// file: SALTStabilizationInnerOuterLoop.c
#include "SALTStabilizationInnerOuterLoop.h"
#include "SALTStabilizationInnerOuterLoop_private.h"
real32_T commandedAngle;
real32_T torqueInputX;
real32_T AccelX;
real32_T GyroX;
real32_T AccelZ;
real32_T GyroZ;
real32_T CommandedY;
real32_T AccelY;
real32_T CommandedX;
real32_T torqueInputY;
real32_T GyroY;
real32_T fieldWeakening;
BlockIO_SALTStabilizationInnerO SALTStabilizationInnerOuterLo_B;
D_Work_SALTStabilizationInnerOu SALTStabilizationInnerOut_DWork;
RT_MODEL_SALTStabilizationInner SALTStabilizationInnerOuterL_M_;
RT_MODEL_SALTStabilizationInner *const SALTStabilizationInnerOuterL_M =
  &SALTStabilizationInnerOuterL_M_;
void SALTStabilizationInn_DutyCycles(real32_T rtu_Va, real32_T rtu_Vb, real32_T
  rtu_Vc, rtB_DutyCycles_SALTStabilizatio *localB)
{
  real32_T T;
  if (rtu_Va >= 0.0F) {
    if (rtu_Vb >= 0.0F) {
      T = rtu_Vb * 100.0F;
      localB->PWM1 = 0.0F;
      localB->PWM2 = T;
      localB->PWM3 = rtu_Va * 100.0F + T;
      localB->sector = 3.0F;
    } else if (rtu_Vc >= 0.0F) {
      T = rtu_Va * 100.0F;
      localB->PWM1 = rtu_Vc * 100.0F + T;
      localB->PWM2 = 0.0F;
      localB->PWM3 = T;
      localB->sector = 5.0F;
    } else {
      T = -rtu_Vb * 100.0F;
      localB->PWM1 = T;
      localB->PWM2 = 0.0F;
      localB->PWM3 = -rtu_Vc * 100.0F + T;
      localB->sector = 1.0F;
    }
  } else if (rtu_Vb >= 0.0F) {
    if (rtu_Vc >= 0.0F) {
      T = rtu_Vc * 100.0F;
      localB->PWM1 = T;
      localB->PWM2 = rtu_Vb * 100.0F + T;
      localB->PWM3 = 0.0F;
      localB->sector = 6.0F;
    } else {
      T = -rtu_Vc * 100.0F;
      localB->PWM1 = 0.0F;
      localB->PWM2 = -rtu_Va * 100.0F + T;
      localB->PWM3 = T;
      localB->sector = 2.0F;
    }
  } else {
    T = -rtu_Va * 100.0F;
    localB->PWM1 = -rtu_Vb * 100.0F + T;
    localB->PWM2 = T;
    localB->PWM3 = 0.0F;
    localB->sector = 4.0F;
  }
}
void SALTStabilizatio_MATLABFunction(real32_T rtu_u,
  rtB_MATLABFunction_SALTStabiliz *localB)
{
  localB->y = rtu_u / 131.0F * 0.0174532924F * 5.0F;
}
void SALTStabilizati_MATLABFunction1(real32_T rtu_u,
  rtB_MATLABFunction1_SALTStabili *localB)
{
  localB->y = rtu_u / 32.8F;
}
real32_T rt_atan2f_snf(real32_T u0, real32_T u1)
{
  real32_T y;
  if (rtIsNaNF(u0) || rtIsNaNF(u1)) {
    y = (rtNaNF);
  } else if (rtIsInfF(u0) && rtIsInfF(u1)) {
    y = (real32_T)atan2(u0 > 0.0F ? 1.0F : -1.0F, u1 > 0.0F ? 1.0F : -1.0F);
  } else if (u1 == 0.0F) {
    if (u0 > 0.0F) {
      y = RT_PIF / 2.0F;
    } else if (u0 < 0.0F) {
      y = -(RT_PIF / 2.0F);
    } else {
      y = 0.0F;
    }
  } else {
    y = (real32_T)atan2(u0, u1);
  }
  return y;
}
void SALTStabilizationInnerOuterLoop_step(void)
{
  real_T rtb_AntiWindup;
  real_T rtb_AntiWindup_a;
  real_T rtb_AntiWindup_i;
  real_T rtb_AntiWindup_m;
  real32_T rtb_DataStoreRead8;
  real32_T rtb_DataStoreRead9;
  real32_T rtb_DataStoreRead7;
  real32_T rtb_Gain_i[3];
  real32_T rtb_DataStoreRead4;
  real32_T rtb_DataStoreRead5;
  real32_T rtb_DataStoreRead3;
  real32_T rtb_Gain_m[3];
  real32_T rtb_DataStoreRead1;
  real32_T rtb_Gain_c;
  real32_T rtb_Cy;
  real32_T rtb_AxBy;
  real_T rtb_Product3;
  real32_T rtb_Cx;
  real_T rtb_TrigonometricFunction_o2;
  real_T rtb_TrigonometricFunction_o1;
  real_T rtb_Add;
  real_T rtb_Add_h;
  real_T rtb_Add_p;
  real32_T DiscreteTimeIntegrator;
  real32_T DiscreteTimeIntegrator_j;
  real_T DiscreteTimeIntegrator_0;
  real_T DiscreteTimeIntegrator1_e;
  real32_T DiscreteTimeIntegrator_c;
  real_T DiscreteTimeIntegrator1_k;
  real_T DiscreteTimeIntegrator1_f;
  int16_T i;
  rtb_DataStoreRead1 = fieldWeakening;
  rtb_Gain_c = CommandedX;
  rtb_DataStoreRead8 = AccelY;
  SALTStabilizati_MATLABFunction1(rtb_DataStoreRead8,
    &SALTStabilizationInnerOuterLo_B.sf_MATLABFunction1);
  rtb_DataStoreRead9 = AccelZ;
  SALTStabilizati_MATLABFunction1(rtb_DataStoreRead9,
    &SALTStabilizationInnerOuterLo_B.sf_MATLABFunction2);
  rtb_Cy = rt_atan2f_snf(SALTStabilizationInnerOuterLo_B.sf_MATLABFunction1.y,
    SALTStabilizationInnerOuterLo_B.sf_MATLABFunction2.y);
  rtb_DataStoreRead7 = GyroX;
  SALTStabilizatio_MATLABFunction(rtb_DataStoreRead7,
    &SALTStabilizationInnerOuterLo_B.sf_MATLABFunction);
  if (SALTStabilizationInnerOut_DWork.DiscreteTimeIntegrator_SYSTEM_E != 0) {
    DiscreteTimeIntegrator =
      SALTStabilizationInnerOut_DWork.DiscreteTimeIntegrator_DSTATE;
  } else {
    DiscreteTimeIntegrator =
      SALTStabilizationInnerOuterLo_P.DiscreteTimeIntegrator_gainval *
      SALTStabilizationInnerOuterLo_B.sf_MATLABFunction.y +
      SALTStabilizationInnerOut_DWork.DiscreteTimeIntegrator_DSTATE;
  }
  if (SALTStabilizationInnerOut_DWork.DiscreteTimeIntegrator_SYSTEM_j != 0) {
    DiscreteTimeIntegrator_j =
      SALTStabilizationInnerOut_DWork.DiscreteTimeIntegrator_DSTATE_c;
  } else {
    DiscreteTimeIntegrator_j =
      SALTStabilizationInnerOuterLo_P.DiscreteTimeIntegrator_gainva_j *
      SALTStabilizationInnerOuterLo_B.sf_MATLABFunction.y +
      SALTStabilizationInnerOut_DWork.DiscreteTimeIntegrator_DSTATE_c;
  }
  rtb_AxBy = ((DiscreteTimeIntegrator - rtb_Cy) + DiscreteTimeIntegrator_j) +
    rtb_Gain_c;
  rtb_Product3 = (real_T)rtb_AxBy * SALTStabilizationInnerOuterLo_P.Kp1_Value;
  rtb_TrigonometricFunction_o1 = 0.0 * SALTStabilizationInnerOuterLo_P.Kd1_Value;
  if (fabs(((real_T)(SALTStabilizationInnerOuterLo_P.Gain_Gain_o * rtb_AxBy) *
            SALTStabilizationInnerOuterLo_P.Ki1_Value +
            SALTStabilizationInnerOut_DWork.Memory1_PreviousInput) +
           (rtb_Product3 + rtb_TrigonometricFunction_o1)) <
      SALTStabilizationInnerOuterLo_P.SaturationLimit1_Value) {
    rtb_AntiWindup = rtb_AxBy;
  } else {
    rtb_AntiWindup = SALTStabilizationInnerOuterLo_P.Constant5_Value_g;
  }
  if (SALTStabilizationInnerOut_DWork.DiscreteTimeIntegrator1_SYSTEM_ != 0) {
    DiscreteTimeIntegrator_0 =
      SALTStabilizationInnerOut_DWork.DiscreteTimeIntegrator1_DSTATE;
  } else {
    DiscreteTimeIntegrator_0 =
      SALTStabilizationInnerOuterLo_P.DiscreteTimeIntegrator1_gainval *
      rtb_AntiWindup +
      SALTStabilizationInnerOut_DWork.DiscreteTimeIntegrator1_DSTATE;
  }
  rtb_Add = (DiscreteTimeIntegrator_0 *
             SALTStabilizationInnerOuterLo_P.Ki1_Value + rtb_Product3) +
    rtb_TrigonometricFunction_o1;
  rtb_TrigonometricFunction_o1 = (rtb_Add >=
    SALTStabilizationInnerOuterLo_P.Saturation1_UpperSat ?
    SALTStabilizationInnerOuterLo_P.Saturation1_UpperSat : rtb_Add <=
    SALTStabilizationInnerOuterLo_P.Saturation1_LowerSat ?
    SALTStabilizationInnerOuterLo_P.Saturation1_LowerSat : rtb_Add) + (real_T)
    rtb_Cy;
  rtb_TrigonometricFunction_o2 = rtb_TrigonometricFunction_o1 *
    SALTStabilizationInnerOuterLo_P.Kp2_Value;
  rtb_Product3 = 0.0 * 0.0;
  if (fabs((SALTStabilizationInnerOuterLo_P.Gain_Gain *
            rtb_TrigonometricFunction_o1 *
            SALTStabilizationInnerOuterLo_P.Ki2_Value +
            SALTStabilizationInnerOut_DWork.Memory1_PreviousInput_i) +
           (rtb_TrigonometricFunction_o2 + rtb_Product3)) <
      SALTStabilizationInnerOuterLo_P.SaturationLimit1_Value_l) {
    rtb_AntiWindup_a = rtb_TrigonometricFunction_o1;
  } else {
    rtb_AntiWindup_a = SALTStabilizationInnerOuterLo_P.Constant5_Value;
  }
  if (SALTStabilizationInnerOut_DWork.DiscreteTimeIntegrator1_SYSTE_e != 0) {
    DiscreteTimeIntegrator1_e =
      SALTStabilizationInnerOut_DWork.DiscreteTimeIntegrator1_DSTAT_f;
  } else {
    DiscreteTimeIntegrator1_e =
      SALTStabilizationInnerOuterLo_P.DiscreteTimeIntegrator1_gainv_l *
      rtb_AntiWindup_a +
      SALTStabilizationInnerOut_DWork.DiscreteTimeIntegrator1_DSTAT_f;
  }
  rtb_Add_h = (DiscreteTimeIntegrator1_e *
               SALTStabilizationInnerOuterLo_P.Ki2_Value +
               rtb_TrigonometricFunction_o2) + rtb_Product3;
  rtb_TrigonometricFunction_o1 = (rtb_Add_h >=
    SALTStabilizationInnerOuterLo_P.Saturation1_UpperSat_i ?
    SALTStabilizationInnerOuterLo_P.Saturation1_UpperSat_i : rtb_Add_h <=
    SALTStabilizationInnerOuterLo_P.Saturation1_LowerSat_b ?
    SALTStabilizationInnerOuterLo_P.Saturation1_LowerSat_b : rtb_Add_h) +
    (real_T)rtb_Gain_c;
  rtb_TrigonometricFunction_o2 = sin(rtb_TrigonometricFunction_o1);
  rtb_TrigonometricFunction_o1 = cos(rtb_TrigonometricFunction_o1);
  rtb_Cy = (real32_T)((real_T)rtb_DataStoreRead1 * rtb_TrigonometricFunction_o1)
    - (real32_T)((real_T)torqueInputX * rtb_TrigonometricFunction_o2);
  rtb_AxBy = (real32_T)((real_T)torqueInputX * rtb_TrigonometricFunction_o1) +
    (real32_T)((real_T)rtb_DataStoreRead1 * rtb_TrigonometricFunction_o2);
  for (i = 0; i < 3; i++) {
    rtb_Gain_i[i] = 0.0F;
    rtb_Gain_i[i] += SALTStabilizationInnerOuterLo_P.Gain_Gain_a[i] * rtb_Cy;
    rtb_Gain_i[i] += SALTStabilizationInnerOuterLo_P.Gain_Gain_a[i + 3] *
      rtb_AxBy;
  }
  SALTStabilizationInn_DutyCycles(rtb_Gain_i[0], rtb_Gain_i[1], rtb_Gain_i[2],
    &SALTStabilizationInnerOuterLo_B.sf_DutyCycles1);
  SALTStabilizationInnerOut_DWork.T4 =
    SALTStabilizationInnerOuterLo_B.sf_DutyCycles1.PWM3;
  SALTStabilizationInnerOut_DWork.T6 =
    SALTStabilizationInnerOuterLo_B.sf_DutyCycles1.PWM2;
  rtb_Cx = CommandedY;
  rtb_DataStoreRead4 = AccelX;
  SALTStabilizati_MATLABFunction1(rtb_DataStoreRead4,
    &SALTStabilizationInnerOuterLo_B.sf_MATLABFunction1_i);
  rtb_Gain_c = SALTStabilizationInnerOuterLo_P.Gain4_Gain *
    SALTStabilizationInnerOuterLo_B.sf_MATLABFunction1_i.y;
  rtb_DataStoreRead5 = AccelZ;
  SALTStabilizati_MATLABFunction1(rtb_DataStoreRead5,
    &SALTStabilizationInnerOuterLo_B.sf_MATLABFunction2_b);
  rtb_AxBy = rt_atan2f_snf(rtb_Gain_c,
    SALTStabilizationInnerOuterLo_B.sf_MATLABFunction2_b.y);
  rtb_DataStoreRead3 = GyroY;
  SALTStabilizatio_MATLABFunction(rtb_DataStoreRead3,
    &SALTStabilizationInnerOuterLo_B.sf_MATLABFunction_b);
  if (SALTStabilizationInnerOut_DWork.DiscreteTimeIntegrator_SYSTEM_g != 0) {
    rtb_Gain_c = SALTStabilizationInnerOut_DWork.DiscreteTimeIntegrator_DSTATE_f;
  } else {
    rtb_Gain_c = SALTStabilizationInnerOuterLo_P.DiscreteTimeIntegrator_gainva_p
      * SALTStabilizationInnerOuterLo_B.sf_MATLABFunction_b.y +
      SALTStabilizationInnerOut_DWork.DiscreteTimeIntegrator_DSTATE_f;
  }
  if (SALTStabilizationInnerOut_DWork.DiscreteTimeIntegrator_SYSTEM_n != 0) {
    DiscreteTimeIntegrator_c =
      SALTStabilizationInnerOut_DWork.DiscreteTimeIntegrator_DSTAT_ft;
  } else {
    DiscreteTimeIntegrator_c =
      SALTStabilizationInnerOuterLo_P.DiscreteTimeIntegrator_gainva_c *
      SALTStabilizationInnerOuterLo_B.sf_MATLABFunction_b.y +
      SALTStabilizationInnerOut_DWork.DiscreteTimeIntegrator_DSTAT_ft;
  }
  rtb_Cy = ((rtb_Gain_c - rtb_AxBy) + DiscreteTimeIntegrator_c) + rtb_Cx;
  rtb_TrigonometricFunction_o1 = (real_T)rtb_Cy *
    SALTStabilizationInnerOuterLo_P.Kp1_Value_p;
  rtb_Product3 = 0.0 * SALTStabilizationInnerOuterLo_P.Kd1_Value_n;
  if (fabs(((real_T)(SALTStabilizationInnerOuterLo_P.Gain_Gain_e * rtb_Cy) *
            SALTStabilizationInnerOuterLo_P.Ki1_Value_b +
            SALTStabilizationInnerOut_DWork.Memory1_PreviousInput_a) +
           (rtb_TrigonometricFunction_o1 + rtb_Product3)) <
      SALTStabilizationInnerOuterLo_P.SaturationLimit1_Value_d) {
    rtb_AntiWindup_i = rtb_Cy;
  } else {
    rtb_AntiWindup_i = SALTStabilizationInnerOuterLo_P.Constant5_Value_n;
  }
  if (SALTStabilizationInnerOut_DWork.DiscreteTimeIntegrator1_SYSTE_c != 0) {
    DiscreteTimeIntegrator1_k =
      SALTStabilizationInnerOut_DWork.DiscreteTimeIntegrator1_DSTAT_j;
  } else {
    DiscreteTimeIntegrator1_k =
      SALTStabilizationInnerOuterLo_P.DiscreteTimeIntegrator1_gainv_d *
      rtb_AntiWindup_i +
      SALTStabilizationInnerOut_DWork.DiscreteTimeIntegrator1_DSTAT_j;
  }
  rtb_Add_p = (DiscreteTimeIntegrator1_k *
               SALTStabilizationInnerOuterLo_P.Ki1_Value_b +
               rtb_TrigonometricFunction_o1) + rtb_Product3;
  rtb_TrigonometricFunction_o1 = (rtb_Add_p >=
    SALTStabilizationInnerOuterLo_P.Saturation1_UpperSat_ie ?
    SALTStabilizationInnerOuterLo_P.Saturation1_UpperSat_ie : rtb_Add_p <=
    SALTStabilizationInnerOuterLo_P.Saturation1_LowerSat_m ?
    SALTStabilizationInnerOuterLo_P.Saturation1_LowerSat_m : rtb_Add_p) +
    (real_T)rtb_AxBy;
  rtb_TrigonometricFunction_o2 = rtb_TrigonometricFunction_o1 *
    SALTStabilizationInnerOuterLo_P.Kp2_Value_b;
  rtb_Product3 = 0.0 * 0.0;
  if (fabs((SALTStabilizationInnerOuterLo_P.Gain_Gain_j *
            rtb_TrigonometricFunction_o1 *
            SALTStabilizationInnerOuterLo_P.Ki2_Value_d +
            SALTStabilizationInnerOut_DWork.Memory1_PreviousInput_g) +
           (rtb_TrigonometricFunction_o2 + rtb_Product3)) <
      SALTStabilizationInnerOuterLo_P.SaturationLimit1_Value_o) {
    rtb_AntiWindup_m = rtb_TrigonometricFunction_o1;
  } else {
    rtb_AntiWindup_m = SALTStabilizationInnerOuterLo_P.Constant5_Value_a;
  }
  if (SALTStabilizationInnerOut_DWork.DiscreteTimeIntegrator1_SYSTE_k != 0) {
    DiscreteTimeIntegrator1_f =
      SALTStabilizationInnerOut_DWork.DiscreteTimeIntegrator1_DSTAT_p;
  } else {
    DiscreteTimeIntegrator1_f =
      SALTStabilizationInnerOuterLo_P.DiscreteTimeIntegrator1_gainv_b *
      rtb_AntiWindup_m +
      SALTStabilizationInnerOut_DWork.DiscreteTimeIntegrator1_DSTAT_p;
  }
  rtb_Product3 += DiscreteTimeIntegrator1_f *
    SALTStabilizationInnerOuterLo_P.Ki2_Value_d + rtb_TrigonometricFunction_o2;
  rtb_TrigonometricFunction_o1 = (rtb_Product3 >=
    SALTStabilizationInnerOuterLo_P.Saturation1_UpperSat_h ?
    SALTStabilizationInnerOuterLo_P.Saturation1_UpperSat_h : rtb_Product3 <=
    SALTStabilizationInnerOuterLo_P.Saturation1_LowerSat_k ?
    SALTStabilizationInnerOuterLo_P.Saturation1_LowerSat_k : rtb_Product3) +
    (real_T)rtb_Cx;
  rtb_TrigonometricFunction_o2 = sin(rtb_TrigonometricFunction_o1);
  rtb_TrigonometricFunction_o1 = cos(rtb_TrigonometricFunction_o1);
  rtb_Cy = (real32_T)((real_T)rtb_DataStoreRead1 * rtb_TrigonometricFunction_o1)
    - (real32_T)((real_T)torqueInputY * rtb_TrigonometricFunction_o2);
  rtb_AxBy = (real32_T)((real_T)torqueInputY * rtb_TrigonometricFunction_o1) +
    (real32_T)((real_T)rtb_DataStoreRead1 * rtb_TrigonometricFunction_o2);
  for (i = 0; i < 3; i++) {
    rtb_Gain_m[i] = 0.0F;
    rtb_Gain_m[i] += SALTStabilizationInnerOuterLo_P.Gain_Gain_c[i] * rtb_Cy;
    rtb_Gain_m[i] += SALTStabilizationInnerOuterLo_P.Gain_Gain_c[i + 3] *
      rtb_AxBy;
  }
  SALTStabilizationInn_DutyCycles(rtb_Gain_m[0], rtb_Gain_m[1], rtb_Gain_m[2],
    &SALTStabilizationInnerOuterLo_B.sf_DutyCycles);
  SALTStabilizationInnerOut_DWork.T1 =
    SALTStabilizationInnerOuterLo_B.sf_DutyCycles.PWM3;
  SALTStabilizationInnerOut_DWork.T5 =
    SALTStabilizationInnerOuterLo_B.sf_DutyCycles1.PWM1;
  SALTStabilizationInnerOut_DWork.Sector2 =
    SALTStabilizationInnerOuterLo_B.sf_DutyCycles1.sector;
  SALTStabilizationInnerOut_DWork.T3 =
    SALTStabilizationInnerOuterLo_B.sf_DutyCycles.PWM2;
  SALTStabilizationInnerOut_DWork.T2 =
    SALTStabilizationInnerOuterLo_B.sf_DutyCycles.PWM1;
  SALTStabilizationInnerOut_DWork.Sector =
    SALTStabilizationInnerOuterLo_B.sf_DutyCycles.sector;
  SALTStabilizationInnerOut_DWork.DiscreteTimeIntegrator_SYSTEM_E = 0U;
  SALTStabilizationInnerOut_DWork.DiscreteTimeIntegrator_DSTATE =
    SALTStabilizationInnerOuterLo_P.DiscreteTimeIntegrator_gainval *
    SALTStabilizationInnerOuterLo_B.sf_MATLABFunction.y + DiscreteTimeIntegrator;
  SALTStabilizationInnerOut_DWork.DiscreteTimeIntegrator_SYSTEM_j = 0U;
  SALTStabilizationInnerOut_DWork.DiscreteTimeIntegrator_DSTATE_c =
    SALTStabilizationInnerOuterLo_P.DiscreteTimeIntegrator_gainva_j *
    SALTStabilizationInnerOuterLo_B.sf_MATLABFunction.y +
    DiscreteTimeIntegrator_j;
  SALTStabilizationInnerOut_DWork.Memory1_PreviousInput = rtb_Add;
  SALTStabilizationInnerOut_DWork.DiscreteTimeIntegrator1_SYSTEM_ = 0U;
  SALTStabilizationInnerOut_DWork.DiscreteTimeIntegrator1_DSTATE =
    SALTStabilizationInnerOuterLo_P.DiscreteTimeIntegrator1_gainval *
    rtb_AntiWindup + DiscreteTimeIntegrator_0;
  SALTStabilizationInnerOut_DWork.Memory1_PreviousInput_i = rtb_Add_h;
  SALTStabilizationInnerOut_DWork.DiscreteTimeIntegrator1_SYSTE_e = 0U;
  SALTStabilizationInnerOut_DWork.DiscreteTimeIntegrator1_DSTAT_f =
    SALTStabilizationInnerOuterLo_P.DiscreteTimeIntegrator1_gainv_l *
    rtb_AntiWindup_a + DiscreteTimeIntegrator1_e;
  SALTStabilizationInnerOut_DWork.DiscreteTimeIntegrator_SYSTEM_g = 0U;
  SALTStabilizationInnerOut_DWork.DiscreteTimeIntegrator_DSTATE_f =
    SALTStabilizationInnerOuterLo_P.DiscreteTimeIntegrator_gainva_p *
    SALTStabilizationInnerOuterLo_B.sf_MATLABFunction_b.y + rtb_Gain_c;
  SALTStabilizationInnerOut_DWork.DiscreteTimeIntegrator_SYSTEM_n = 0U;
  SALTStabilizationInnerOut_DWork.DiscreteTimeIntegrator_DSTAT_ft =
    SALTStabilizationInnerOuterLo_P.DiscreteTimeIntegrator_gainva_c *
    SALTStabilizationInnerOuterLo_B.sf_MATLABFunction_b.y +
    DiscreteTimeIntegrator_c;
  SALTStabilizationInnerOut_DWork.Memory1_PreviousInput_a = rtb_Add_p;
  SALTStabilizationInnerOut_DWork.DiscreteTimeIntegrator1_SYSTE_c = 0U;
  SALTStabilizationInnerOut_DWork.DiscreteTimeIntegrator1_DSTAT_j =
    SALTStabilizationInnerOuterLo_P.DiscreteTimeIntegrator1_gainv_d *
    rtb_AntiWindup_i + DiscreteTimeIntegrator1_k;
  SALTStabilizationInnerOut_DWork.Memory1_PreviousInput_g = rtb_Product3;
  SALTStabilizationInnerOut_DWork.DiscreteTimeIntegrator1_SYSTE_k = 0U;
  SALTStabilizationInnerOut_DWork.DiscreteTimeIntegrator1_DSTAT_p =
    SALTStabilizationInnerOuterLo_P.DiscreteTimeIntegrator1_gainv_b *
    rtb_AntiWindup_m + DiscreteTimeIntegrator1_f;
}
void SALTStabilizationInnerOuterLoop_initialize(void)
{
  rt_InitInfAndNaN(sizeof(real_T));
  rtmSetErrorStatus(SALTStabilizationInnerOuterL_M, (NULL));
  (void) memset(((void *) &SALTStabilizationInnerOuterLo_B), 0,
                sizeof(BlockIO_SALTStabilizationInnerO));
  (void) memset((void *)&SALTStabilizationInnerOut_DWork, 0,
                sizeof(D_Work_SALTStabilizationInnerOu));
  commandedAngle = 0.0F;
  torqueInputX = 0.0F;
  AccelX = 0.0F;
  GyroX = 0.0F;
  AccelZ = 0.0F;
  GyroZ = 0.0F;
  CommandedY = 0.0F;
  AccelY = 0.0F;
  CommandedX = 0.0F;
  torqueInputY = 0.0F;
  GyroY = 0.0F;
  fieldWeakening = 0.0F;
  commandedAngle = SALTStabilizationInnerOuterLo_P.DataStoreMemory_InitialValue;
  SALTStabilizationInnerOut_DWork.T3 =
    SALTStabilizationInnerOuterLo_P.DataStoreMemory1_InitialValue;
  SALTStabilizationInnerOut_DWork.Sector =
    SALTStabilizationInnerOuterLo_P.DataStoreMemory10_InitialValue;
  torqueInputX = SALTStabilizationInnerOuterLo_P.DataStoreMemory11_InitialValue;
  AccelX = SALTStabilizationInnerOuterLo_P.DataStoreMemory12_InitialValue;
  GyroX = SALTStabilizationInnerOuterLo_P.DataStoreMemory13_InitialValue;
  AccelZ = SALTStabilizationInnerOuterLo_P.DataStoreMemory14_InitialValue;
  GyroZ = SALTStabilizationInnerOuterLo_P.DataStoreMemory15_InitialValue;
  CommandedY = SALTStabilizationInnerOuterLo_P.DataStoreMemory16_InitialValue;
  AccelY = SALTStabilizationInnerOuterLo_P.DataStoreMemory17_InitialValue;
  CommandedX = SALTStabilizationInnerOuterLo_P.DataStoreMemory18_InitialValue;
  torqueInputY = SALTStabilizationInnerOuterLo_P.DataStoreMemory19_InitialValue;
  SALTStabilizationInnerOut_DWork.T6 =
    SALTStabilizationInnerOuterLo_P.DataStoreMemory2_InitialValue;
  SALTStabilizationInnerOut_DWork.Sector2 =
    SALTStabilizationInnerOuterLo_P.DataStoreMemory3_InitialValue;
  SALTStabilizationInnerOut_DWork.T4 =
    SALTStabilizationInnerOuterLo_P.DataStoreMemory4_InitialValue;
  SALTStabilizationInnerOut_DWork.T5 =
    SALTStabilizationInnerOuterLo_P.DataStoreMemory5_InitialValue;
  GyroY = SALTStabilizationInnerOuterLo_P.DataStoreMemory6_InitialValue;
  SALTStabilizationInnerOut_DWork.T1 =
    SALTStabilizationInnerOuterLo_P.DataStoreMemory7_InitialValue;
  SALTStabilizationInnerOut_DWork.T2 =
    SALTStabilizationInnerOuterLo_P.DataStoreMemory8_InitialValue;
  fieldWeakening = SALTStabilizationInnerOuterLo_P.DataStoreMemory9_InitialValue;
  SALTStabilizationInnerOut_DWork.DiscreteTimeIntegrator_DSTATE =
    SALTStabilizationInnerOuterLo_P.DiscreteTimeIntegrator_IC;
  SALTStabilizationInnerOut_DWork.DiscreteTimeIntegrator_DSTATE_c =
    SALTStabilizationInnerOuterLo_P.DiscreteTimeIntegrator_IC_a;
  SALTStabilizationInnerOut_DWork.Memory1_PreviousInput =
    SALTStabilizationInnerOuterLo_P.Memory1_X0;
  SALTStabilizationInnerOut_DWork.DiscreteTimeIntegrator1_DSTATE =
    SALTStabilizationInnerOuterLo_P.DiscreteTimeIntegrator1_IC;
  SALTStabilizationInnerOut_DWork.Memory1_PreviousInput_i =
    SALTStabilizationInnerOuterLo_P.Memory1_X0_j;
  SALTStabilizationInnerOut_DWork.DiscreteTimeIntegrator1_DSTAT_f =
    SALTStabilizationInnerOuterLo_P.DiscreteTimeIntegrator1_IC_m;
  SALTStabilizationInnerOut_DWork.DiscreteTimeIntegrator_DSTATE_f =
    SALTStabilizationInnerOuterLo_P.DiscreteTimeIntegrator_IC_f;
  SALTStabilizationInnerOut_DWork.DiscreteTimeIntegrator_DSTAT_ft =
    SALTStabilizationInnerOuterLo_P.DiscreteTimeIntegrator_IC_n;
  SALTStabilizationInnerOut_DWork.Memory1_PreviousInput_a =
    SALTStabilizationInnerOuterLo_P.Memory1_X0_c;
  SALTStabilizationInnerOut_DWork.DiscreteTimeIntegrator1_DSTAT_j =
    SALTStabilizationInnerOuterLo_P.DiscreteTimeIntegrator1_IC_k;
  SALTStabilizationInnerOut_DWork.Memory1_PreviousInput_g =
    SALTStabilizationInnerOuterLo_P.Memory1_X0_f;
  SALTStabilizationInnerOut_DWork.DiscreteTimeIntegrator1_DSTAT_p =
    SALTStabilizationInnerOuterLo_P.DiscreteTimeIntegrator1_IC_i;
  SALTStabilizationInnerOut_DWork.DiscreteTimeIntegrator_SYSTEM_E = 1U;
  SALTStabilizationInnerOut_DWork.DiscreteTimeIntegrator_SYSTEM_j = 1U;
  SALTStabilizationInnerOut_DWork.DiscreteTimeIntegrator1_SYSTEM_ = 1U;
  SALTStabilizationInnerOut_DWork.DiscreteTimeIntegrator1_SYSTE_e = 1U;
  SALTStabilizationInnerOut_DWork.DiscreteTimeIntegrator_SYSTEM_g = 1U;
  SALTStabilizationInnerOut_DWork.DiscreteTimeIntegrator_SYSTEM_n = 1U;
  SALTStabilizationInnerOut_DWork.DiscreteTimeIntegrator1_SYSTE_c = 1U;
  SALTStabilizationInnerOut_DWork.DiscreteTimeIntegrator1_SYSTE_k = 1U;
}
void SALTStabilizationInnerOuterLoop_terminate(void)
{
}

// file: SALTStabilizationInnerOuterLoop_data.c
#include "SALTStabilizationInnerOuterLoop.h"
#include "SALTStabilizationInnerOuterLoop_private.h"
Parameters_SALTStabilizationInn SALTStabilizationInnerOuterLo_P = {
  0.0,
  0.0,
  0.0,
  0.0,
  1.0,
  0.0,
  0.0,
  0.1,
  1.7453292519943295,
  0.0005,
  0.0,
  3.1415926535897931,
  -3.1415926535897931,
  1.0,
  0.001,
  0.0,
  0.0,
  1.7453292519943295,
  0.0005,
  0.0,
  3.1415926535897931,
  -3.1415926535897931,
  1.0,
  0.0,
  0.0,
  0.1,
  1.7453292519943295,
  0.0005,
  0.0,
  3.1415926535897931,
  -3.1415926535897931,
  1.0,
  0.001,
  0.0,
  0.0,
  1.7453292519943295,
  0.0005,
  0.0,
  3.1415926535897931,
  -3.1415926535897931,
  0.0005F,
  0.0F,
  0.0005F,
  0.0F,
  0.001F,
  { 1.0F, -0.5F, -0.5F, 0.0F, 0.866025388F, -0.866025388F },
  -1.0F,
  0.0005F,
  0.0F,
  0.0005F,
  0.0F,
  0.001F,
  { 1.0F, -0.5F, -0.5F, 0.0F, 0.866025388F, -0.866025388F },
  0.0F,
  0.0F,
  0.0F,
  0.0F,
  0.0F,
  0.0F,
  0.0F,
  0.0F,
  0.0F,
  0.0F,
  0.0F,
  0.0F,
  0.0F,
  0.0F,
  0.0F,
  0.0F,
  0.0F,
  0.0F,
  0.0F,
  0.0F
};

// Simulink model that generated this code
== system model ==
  DataStoreMemory : DataStoreMemory  DataStoreName=commandedAngle
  DataStoreMemory11 : DataStoreMemory  DataStoreName=torqueInputX
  DataStoreMemory12 : DataStoreMemory  DataStoreName=AccelX
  DataStoreMemory13 : DataStoreMemory  DataStoreName=GyroX
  DataStoreMemory14 : DataStoreMemory  DataStoreName=AccelZ
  DataStoreMemory15 : DataStoreMemory  DataStoreName=GyroZ
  DataStoreMemory16 : DataStoreMemory  DataStoreName=CommandedY
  DataStoreMemory17 : DataStoreMemory  DataStoreName=AccelY
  DataStoreMemory18 : DataStoreMemory  DataStoreName=CommandedX
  DataStoreMemory19 : DataStoreMemory  DataStoreName=torqueInputY
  DataStoreMemory6 : DataStoreMemory  DataStoreName=GyroY
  DataStoreMemory9 : DataStoreMemory  DataStoreName=fieldWeakening
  DataStoreWrite#1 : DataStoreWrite  DataStoreName=T4  <- 1: DutyCycles1/3
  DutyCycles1 : MATLAB Function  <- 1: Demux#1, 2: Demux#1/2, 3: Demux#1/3
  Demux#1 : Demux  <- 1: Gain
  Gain : Gain  Gain=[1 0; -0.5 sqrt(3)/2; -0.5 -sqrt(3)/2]  Multiplication=Matrix(K*u)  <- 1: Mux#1
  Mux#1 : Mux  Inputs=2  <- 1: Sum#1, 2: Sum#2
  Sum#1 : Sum  Inputs=+-  <- 1: Product#1, 2: Product#2
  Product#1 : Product  <- 1: DataStoreRead1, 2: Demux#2
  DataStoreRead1 : DataStoreRead  DataStoreName=fieldWeakening
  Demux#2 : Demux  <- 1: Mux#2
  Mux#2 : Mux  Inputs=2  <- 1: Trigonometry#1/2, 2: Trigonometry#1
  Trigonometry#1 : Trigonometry  Operator=sincos  <- 1: Sum#3
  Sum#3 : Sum  <- 1: DataStoreRead#1, 2: Saturation1
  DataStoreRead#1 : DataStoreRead  DataStoreName=CommandedX
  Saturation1 : Saturate  UpperLimit=pi  LowerLimit=-pi  <- 1: Add
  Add : Sum  Inputs=+++  <- 1: Product#3, 2: Product#4, 3: Product3
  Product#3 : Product  <- 1: Sum#4, 2: Kp2
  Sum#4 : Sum  <- 1: TrigonometricFunction, 2: Saturate#1
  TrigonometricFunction : Trigonometry  Operator=atan2  <- 1: MATLABFunction1, 2: MATLABFunction2
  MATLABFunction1 : MATLAB Function  <- 1: DataTypeConversion#1
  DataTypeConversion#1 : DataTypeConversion  <- 1: DataStoreRead8
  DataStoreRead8 : DataStoreRead  DataStoreName=AccelY
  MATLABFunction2 : MATLAB Function  <- 1: DataTypeConversion#2
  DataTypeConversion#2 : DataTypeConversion  <- 1: DataStoreRead9
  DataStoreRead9 : DataStoreRead  DataStoreName=AccelZ
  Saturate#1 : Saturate  UpperLimit=pi  LowerLimit=-pi  <- 1: Sum#5
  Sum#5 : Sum  Inputs=+++  <- 1: Product#5, 2: Product#6, 3: Product#7
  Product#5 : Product  <- 1: Sum#6, 2: Kp1
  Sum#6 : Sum  <- 1: DataStoreRead#1, 2: Sum#7
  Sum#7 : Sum  <- 1: Sum#8, 2: DiscreteTimeIntegrator
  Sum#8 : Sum  Inputs=+-  <- 1: DiscreteIntegrator#1, 2: TrigonometricFunction
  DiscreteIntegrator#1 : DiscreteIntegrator  IntegratorMethod=Integration: Trapezoidal  UpperSaturationLimit=1  LowerSaturationLimit=-1  <- 1: MATLABFunction
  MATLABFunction : MATLAB Function  <- 1: DataTypeConversion#3
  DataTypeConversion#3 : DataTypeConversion  <- 1: DataStoreRead7
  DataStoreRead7 : DataStoreRead  DataStoreName=GyroX
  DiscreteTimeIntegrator : DiscreteIntegrator  IntegratorMethod=Integration: Trapezoidal  <- 1: MATLABFunction
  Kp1 : Constant
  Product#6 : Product  <- 1: DiscreteTimeIntegrator1, 2: Ki1
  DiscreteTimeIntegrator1 : DiscreteIntegrator  IntegratorMethod=Integration: Trapezoidal  <- 1: AntiWindup
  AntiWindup : Switch  Threshold=0.5  <- 1: Sum#6, 2: RelationalOperator#1, 3: Constant5
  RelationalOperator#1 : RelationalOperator  Operator=<  <- 1: Abs#1, 2: SaturationLimit1
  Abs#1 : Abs  <- 1: Sum#9
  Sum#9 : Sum  Inputs=+++  <- 1: Product#8, 2: Memory1, 3: Sum#10
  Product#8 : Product  <- 1: Gain#1, 2: Ki1
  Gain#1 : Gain  Gain=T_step  <- 1: Sum#6
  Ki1 : Constant  Value=0
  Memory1 : Memory  <- 1: Sum#5
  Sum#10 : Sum  Inputs=++  <- 1: Product#5, 2: Product#7
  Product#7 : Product  <- 2: Kd1
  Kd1 : Constant  Value=.1
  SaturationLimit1 : Constant  Value=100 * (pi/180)
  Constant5 : Constant  Value=0
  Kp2 : Constant
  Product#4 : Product  <- 1: DiscreteIntegrator#2, 2: Ki2
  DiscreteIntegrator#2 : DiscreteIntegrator  IntegratorMethod=Integration: Trapezoidal  <- 1: Switch#1
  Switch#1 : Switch  Threshold=0.5  <- 1: Sum#4, 2: RelationalOperator#2, 3: Constant#1
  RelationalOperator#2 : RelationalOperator  Operator=<  <- 1: Abs#2, 2: Constant#2
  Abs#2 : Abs  <- 1: Sum#11
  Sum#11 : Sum  Inputs=+++  <- 1: Product#9, 2: Memory#1, 3: Sum#12
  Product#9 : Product  <- 1: Gain#2, 2: Ki2
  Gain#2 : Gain  Gain=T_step  <- 1: Sum#4
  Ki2 : Constant  Value=0
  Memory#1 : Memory  <- 1: Add
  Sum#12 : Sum  Inputs=++  <- 1: Product#3, 2: Product3
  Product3 : Product
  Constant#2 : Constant  Value=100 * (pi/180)
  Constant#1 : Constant  Value=0
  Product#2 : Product  <- 1: DataStoreRead#2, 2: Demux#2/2
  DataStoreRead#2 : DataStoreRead  DataStoreName=torqueInputX
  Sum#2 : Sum  Inputs=++  <- 1: Product#10, 2: AxBy
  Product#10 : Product  <- 1: DataStoreRead#2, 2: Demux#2
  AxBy : Product  <- 1: DataStoreRead1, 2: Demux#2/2
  DataStoreWrite#2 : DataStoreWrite  DataStoreName=T6  <- 1: DutyCycles1/2
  Gain4 : Gain  Gain=-1
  DataStoreWrite#3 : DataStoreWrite  DataStoreName=T1  <- 1: DutyCycles/3
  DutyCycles : MATLAB Function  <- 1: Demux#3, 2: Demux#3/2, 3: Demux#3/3
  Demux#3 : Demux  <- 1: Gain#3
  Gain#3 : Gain  Gain=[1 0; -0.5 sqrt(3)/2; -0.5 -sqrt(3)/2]  Multiplication=Matrix(K*u)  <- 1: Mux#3
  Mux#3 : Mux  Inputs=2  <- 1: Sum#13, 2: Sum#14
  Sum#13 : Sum  Inputs=+-  <- 1: Product#11, 2: Product#12
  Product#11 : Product  <- 1: DataStoreRead1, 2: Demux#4
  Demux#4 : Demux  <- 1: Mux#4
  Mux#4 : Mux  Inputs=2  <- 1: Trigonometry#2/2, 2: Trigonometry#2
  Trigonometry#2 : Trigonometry  Operator=sincos  <- 1: Sum#15
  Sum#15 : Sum  <- 1: DataStoreRead#3, 2: Saturate#2
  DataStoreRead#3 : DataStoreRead  DataStoreName=CommandedY
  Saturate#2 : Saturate  UpperLimit=pi  LowerLimit=-pi  <- 1: Sum#16
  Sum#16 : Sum  Inputs=+++  <- 1: Product#13, 2: Product#14, 3: Product#15
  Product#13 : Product  <- 1: Sum#17, 2: Constant#3
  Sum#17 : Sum  <- 1: Trigonometry#3, 2: Saturate#3
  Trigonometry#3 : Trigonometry  Operator=atan2  <- 1: Gain#4, 2: MATLABFunction#1
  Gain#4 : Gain  Gain=-1  <- 1: MATLABFunction#2
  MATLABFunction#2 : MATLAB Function  <- 1: DataTypeConversion#4
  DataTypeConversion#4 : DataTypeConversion  <- 1: DataStoreRead4
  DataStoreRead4 : DataStoreRead  DataStoreName=AccelX
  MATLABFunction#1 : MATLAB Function  <- 1: DataTypeConversion#5
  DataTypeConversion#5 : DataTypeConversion  <- 1: DataStoreRead5
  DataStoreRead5 : DataStoreRead  DataStoreName=AccelZ
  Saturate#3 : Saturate  UpperLimit=pi  LowerLimit=-pi  <- 1: Sum#18
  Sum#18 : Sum  Inputs=+++  <- 1: Product#16, 2: Product#17, 3: Product#18
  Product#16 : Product  <- 1: Sum#19, 2: Constant#4
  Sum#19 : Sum  <- 1: DataStoreRead#3, 2: Sum#20
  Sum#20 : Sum  <- 1: Sum#21, 2: DiscreteIntegrator#3
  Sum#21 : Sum  Inputs=+-  <- 1: DiscreteIntegrator#4, 2: Trigonometry#3
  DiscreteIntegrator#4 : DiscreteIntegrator  IntegratorMethod=Integration: Trapezoidal  UpperSaturationLimit=1  LowerSaturationLimit=-1  <- 1: MATLABFunction#3
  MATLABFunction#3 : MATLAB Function  <- 1: DataTypeConversion#6
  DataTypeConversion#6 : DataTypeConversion  <- 1: DataStoreRead3
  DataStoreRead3 : DataStoreRead  DataStoreName=GyroY
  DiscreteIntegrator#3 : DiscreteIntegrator  IntegratorMethod=Integration: Trapezoidal  <- 1: MATLABFunction#3
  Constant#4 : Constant
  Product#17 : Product  <- 1: DiscreteIntegrator#5, 2: Constant#5
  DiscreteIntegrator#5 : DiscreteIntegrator  IntegratorMethod=Integration: Trapezoidal  <- 1: Switch#2
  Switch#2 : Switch  Threshold=0.5  <- 1: Sum#19, 2: RelationalOperator#3, 3: Constant#6
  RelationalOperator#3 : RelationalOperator  Operator=<  <- 1: Abs#3, 2: Constant#7
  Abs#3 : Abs  <- 1: Sum#22
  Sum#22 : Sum  Inputs=+++  <- 1: Product#19, 2: Memory#2, 3: Sum#23
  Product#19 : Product  <- 1: Gain#5, 2: Constant#5
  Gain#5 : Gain  Gain=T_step  <- 1: Sum#19
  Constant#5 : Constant  Value=0
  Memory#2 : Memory  <- 1: Sum#18
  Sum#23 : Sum  Inputs=++  <- 1: Product#16, 2: Product#18
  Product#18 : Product  <- 2: Constant#8
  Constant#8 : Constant  Value=.1
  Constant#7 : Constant  Value=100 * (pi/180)
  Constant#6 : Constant  Value=0
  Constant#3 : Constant
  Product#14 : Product  <- 1: DiscreteIntegrator#6, 2: Constant#9
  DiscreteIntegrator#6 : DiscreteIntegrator  IntegratorMethod=Integration: Trapezoidal  <- 1: Switch#3
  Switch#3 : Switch  Threshold=0.5  <- 1: Sum#17, 2: RelationalOperator#4, 3: Constant#10
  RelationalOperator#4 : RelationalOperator  Operator=<  <- 1: Abs#4, 2: Constant#11
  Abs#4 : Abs  <- 1: Sum#24
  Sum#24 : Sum  Inputs=+++  <- 1: Product#20, 2: Memory#3, 3: Sum#25
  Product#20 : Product  <- 1: Gain#6, 2: Constant#9
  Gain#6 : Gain  Gain=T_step  <- 1: Sum#17
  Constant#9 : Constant  Value=0
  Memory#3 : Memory  <- 1: Sum#16
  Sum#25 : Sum  Inputs=++  <- 1: Product#13, 2: Product#15
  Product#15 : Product
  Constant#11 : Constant  Value=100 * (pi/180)
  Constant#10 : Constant  Value=0
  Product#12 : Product  <- 1: DataStoreRead#4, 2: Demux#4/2
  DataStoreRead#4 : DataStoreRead  DataStoreName=torqueInputY
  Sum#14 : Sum  Inputs=++  <- 1: Product#21, 2: Product#22
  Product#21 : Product  <- 1: DataStoreRead#4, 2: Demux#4
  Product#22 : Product  <- 1: DataStoreRead1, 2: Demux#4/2
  DataStoreWrite#4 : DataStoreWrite  DataStoreName=T5  <- 1: DutyCycles1
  DataStoreWrite#5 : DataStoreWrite  DataStoreName=Sector2  <- 1: DutyCycles1/4
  DataStoreWrite#6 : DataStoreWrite  DataStoreName=T3  <- 1: DutyCycles/2
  DataStoreWrite#7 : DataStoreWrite  DataStoreName=T2  <- 1: DutyCycles
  DataStoreWrite#8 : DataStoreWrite  DataStoreName=Sector  <- 1: DutyCycles/4
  DataStoreMemory1 : DataStoreMemory  DataStoreName=T3
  DataStoreMemory10 : DataStoreMemory  DataStoreName=Sector
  DataStoreMemory2 : DataStoreMemory  DataStoreName=T6
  DataStoreMemory3 : DataStoreMemory  DataStoreName=Sector2
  DataStoreMemory4 : DataStoreMemory  DataStoreName=T4
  DataStoreMemory5 : DataStoreMemory  DataStoreName=T5
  DataStoreMemory7 : DataStoreMemory  DataStoreName=T1
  DataStoreMemory8 : DataStoreMemory  DataStoreName=T2
== matlab function MATLAB Function1 ==
function y = fcn(u)
%#codegen

y = u/32.8;

== matlab function MATLAB Function ==
function y = fcn(u)
%#codegen

y = ((u/131) * (pi/180))*5;

== matlab function MATLAB Function2 ==
function y = fcn(u)
%#codegen

y = u/32.8;

== matlab function MATLAB Function ==
function y = fcn(u)
%#codegen

y = ((u/131) * (pi/180))*5;

== matlab function MATLAB Function1 ==
function y = fcn(u)
%#codegen

y = u/32.8;

== matlab function MATLAB Function2 ==
function y = fcn(u)
%#codegen

y = u/32.8;

== matlab function DutyCycles ==
function [PWM1, PWM2, PWM3, sector]  = DutyCycleCalc(Va, Vb, Vc)
%#codegen
PWM = single(100);

Ta = single(0);

if (Va >= 0)
    if (Vb >= 0)
        %Sector 3, 0 - 60 Degrees
        T1 = Vb;
        T2 = Va;
    
        T1 = T1*PWM;
        T2 = T2*PWM;
        Tc = (PWM-T1-T2)/2;
        Tb = Ta + T1;
        Ta = Tb + T2;
    
        PWM1 = single(0);
        PWM2 = Tb;
        PWM3 = Ta;
        sector = single(3);
    else
        if (Vc >= 0)
           %Sector 5, 120 - 180 Degrees
            T1 = Va;
            T2 = Vc;
    
            T1 = T1*PWM;
            T2 = T2*PWM;
            Tc = (PWM-T1-T2)/2;
            Tb = Ta + T1;
            Ta = Tb + T2;
    
            PWM1 = Ta;
            PWM2 = single(0);
            PWM3 = Tb;
            sector = single(5);
        else
            %Sector 1, 60 - 120 Degrees
            T1 = -Vb;
            T2 = -Vc;
    
            T1 = T1*PWM;
            T2 = T2*PWM;
            Tc = (PWM-T1-T2)/2;
            Tb = Ta + T1;
            Ta = Tb + T2;
    
            PWM1 = Tb;
            PWM2 = single(0);
            PWM3 = Ta;
            sector = single(1);
        end
    end
else
    if (Vb >= 0)
        if (Vc >= 0)
            %Sector 6, 240 - 300 Degrees
            T1 = Vc;
            T2 = Vb;
    
            T1 = T1*PWM;
            T2 = T2*PWM;
            Tc = (PWM-T1-T2)/2;
            Tb = Ta + T1;
            Ta = Tb + T2;
    
            PWM1 = Tb;
            PWM2 = Ta;
            PWM3 = single(0);
            sector = single(6);
        else
            %Sector 2, 300 - 0 Degrees
            T1 = -Vc;
            T2 = -Va;
    
            T1 = T1*PWM;
            T2 = T2*PWM;
            Tc = (PWM-T1-T2)/2;
            Tb = Ta + T1;
            Ta = Tb + T2;
    
            PWM1 = single(0);
            PWM2 = Ta;
            PWM3 = Tb;
            sector = single(2);
        end
    else
        %Sector 4, 180 - 240 Degrees
        T1 = -Va;
        T2 = -Vb;
    
        T1 = T1*PWM;
        T2 = T2*PWM;
        Tc = (PWM-T1-T2)/2;
        Tb = Ta + T1;
        Ta = Tb + T2;
    
        PWM1 = Ta;
        PWM2 = Tb;
        PWM3 = single(0);
        sector = single(4);
    end
end

end

== matlab function DutyCycles1 ==
function [PWM1, PWM2, PWM3, sector]  = DutyCycleCalc(Va, Vb, Vc)
%#codegen
PWM = single(100);

Ta = single(0);

if (Va >= 0)
    if (Vb >= 0)
        %Sector 3, 0 - 60 Degrees
        T1 = Vb;
        T2 = Va;
    
        T1 = T1*PWM;
        T2 = T2*PWM;
        Tc = (PWM-T1-T2)/2;
        Tb = Ta + T1;
        Ta = Tb + T2;
    
        PWM1 = single(0);
        PWM2 = Tb;
        PWM3 = Ta;
        sector = single(3);
    else
        if (Vc >= 0)
           %Sector 5, 120 - 180 Degrees
            T1 = Va;
            T2 = Vc;
    
            T1 = T1*PWM;
            T2 = T2*PWM;
            Tc = (PWM-T1-T2)/2;
            Tb = Ta + T1;
            Ta = Tb + T2;
    
            PWM1 = Ta;
            PWM2 = single(0);
            PWM3 = Tb;
            sector = single(5);
        else
            %Sector 1, 60 - 120 Degrees
            T1 = -Vb;
            T2 = -Vc;
    
            T1 = T1*PWM;
            T2 = T2*PWM;
            Tc = (PWM-T1-T2)/2;
            Tb = Ta + T1;
            Ta = Tb + T2;
    
            PWM1 = Tb;
            PWM2 = single(0);
            PWM3 = Ta;
            sector = single(1);
        end
    end
else
    if (Vb >= 0)
        if (Vc >= 0)
            %Sector 6, 240 - 300 Degrees
            T1 = Vc;
            T2 = Vb;
    
            T1 = T1*PWM;
            T2 = T2*PWM;
            Tc = (PWM-T1-T2)/2;
            Tb = Ta + T1;
            Ta = Tb + T2;
    
            PWM1 = Tb;
            PWM2 = Ta;
            PWM3 = single(0);
            sector = single(6);
        else
            %Sector 2, 300 - 0 Degrees
            T1 = -Vc;
            T2 = -Va;
    
            T1 = T1*PWM;
            T2 = T2*PWM;
            Tc = (PWM-T1-T2)/2;
            Tb = Ta + T1;
            Ta = Tb + T2;
    
            PWM1 = single(0);
            PWM2 = Ta;
            PWM3 = Tb;
            sector = single(2);
        end
    else
        %Sector 4, 180 - 240 Degrees
        T1 = -Va;
        T2 = -Vb;
    
        T1 = T1*PWM;
        T2 = T2*PWM;
        Tc = (PWM-T1-T2)/2;
        Tb = Ta + T1;
        Ta = Tb + T2;
    
        PWM1 = Ta;
        PWM2 = Tb;
        PWM3 = single(0);
        sector = single(4);
    end
end

end
